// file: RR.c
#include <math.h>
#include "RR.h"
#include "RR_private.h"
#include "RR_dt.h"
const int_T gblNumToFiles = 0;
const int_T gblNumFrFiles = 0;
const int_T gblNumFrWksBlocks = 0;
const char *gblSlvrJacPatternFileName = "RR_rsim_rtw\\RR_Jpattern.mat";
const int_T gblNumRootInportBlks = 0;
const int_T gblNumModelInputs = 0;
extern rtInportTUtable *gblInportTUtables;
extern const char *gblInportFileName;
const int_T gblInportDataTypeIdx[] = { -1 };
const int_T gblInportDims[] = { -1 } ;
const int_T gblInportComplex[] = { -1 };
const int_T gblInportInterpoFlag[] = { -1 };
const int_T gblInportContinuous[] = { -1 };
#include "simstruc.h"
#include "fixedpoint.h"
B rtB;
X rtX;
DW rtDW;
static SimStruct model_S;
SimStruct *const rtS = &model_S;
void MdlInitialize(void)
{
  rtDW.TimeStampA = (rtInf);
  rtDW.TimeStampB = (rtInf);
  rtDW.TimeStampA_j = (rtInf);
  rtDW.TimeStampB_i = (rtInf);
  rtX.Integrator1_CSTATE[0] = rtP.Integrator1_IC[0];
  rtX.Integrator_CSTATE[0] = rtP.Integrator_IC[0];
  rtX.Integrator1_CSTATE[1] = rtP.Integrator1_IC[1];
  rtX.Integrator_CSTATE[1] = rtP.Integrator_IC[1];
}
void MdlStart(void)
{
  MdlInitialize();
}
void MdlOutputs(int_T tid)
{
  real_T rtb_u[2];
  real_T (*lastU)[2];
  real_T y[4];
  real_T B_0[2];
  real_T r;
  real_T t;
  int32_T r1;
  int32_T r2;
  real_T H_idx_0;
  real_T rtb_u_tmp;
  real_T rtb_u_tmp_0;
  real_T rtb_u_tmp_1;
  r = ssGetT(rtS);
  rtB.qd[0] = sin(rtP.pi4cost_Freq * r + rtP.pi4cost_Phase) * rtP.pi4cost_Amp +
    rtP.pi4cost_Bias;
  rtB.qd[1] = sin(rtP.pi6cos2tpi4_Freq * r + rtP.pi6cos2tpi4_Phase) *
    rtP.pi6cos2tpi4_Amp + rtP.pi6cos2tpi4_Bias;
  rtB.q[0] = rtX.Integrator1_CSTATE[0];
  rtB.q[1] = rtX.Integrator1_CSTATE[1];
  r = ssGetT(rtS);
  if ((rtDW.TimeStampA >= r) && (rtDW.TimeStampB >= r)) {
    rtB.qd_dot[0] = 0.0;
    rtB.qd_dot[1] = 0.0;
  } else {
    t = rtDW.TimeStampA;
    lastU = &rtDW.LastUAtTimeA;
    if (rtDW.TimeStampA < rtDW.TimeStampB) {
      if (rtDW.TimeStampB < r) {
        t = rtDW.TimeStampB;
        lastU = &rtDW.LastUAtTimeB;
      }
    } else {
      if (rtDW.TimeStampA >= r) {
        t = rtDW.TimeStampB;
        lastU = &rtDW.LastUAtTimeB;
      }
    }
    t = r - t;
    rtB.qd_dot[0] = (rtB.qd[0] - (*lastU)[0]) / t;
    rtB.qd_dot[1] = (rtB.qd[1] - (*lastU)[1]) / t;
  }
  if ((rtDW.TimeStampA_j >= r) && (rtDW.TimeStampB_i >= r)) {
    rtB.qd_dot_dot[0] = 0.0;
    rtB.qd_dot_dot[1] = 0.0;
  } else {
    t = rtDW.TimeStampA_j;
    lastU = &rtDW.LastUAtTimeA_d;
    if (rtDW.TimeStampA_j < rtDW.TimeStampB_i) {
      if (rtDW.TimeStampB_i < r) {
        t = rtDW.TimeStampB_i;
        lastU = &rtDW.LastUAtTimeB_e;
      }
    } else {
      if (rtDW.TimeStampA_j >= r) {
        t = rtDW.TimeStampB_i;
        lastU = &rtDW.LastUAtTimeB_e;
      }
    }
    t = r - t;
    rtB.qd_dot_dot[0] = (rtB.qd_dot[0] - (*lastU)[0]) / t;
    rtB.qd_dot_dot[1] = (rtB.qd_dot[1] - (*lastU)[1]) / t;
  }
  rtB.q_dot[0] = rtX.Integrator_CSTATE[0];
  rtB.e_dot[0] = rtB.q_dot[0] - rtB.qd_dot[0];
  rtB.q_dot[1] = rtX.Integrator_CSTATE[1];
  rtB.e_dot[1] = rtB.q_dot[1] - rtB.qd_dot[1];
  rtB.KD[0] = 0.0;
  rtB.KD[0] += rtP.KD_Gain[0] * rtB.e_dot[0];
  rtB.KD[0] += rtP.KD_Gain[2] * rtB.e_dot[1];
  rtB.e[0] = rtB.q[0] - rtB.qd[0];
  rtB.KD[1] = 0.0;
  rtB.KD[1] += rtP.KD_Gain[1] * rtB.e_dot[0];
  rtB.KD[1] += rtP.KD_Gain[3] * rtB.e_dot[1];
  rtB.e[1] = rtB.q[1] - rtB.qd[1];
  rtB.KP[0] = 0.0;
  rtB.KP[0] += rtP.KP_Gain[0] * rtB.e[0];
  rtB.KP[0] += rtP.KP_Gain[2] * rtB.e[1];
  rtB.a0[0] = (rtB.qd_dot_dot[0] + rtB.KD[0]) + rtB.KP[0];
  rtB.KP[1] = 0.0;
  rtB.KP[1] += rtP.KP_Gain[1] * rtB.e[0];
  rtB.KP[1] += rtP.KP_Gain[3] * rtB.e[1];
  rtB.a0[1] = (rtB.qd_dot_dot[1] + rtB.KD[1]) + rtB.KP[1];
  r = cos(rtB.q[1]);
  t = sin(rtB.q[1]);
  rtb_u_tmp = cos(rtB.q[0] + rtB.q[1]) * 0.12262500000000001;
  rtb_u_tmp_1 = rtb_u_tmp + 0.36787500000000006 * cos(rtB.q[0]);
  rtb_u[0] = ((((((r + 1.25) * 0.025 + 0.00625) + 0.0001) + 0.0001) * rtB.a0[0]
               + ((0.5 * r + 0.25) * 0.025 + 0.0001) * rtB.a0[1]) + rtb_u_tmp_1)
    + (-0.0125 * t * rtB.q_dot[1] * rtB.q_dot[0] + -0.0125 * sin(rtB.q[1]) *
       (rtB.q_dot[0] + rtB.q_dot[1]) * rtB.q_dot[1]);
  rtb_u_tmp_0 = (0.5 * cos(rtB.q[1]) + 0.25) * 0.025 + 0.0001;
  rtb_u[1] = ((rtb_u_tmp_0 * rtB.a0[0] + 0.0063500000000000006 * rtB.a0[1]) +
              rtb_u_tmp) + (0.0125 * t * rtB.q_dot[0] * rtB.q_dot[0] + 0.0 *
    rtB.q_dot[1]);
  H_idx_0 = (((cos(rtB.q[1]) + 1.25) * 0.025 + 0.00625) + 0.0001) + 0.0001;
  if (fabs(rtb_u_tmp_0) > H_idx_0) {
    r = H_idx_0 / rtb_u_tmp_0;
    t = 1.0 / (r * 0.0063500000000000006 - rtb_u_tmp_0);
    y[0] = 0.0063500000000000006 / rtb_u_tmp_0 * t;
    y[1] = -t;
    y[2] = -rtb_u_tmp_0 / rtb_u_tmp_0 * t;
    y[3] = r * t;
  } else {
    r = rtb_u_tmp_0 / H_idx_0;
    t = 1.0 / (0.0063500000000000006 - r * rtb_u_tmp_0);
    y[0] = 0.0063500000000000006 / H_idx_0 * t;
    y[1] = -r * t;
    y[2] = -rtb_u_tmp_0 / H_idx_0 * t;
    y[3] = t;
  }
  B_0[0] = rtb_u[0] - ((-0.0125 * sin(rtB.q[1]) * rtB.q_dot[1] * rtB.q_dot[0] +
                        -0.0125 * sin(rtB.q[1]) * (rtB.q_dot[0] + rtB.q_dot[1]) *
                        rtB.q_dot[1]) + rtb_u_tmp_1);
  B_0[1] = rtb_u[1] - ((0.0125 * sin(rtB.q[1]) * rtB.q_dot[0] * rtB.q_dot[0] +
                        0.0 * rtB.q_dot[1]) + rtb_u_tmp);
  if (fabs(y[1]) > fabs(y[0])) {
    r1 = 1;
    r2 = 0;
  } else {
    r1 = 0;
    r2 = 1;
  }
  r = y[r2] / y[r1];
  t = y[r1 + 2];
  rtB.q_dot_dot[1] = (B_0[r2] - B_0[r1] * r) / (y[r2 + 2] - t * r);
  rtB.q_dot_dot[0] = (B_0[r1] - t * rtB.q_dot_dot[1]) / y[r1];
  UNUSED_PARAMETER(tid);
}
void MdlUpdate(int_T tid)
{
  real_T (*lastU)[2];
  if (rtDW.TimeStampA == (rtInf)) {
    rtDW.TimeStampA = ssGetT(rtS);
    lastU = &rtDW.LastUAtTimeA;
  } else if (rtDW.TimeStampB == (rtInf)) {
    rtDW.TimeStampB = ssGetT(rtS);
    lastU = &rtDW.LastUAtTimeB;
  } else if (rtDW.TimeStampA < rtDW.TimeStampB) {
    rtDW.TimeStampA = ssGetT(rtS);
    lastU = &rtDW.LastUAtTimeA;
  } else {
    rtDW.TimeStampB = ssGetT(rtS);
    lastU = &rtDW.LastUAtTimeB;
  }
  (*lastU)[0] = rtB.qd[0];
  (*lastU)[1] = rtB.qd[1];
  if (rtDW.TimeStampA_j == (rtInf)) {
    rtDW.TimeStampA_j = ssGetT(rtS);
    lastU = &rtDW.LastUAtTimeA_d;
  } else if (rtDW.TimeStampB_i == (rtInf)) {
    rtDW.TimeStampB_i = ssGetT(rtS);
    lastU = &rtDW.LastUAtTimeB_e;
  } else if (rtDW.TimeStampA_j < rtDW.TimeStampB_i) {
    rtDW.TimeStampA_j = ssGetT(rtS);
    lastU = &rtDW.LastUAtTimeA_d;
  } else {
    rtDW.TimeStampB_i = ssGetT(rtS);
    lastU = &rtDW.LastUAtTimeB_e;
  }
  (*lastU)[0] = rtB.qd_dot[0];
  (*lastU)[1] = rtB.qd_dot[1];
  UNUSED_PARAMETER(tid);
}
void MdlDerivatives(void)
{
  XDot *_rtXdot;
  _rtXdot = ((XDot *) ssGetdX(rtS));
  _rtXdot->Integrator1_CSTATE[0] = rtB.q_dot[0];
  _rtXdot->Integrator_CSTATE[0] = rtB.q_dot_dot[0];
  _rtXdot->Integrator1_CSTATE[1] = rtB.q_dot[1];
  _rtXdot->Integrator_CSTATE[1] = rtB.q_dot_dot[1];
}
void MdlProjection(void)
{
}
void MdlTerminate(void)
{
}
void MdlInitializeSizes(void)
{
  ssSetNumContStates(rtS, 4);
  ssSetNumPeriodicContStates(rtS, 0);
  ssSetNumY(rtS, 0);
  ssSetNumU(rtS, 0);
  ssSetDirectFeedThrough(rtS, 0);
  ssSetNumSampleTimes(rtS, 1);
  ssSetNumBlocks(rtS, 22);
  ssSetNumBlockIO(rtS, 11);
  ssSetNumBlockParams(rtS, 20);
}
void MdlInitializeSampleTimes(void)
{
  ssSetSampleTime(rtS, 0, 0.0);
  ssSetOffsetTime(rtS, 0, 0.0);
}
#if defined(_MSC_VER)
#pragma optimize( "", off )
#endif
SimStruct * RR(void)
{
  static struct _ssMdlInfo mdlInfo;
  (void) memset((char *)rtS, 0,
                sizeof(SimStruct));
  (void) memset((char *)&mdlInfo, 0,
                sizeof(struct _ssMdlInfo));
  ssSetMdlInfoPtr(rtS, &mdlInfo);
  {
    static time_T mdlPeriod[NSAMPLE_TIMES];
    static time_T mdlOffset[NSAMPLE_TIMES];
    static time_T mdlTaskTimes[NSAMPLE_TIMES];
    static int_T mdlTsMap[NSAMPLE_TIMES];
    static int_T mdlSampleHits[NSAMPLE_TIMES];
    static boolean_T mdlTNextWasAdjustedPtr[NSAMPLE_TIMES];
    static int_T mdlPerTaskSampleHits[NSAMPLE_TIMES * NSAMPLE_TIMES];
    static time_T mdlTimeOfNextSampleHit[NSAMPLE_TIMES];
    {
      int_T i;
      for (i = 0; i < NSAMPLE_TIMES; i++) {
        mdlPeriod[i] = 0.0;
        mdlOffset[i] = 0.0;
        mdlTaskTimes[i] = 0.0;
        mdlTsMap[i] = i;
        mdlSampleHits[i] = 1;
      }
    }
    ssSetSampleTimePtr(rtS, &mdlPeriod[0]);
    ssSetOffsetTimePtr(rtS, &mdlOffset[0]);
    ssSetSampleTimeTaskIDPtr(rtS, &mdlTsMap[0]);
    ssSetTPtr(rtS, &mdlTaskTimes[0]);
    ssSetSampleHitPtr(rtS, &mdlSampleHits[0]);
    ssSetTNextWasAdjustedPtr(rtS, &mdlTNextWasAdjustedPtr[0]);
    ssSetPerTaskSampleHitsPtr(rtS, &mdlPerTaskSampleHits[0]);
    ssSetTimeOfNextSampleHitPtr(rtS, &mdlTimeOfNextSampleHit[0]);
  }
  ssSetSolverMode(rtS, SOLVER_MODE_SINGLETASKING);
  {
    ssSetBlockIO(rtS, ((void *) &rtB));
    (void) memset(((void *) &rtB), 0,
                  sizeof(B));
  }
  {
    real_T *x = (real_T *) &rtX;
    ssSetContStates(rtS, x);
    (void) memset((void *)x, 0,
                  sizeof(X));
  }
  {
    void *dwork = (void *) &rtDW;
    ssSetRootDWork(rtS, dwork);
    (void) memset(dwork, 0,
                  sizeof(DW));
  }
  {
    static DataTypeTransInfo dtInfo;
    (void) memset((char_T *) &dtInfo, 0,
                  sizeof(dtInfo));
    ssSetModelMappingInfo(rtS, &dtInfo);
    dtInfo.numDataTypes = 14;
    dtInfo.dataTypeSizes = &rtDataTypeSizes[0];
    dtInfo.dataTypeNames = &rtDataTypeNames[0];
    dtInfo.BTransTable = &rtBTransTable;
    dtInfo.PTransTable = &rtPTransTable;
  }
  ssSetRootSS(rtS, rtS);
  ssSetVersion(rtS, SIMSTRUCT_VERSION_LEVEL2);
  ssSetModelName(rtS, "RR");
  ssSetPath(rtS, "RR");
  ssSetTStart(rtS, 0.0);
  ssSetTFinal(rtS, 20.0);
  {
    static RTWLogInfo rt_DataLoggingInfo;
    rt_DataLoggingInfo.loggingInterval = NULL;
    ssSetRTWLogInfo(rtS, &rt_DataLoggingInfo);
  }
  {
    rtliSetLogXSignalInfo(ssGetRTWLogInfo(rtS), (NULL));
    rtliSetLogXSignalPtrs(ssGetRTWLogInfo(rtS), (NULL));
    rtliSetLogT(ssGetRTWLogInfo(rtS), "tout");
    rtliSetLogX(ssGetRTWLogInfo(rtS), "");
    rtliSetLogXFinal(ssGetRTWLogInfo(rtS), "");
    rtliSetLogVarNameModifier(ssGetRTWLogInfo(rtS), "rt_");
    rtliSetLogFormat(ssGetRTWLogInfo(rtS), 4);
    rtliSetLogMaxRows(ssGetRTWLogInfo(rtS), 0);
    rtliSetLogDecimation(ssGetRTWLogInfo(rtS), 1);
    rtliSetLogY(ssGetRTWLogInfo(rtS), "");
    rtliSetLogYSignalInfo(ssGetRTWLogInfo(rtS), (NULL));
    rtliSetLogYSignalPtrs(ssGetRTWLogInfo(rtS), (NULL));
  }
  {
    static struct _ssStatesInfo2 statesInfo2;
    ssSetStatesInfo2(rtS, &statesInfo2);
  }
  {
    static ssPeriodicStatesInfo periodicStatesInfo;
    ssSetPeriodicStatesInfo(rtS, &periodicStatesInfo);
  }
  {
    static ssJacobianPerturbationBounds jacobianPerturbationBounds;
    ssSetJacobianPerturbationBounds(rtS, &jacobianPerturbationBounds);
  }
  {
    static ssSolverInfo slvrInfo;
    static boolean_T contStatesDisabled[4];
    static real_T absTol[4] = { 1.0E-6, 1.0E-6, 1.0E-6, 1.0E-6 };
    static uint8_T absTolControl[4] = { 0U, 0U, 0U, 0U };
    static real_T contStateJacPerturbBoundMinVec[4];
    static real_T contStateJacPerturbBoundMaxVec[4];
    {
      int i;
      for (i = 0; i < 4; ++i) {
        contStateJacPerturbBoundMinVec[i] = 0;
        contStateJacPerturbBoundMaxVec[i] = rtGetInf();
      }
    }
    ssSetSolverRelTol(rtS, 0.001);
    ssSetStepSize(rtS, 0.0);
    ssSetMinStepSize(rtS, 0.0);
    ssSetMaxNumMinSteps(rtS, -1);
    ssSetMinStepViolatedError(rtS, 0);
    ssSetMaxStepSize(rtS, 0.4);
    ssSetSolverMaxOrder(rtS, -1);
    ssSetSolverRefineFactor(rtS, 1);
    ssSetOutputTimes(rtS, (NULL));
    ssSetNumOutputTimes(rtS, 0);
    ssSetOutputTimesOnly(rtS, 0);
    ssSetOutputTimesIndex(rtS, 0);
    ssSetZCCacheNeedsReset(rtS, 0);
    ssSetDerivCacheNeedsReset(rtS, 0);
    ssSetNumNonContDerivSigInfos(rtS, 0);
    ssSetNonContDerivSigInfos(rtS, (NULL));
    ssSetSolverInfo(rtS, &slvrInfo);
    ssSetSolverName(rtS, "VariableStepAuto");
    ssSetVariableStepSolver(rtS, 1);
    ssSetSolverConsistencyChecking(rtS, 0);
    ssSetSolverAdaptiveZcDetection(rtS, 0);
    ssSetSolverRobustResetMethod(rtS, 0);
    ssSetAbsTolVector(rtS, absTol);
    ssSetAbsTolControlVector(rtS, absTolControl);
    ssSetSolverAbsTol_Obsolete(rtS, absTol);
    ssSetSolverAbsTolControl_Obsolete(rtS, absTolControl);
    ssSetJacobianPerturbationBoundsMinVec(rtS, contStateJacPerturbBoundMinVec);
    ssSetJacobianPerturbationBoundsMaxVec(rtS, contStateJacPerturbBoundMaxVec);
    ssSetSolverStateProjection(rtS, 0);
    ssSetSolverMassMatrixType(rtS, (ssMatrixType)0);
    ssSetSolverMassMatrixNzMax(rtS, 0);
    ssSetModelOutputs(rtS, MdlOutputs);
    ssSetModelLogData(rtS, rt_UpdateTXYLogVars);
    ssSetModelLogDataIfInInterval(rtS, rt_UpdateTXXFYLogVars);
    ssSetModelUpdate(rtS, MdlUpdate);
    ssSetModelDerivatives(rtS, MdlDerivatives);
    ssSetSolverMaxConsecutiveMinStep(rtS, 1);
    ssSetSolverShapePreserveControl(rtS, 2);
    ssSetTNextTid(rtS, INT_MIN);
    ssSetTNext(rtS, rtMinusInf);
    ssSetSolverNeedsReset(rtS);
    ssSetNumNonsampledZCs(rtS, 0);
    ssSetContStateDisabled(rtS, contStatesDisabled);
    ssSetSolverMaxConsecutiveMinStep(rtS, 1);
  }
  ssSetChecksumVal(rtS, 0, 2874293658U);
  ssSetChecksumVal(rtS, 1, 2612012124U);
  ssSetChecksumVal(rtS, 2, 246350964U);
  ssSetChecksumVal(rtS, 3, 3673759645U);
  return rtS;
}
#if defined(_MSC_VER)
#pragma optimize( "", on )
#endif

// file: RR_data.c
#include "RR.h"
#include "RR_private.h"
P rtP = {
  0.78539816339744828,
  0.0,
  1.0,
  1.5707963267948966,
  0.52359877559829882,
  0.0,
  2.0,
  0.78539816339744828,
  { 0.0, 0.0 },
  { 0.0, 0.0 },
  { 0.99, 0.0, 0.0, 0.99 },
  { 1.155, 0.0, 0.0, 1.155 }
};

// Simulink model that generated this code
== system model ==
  Derivative#1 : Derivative  <- 1: qd
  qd : MATLAB Function  <- 1: pi4cost, 2: pi6cos2tpi4
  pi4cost : Sin  Amplitude=pi/4  Phase=pi/2
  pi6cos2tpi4 : Sin  Amplitude=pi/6  Frequency=2  Phase=pi/4
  Derivative#2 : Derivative  <- 1: Derivative#1
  Integrator1 : Integrator  InitialCondition=[0;0]  <- 1: Integrator
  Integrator : Integrator  InitialCondition=[0;0]  <- 1: MATLABFunction#1
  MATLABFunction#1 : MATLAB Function  <- 1: MATLABFunction#2, 2: Integrator1, 3: Integrator
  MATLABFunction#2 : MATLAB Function  <- 1: Sum#1, 2: Integrator1, 3: Integrator
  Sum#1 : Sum  Inputs=+++  <- 1: Derivative#2, 2: KD, 3: KP
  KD : Gain  Gain=[0.99 0;0 0.99]  Multiplication=Matrix(K*u) (u vector)  <- 1: Sum#2
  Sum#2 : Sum  Inputs=-+  <- 1: Derivative#1, 2: Integrator
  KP : Gain  Gain=[1.155 0;0 1.155]  Multiplication=Matrix(K*u) (u vector)  <- 1: Sum#3
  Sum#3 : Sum  Inputs=-+  <- 1: qd, 2: Integrator1
== matlab function MATLABFunction#2 ==
function u  = Control(a0,q,q_dot)
q1=q(1,1);
q2=q(2,1);
q1_dot=q_dot(1,1);
q2_dot=q_dot(2,1);
m1=0.025;
m2=0.025;
l1=1;
lc1=0.5;
lc2=0.5;
q2=q(2,1);
q1_dot=q_dot(1,1);
q2_dot=q_dot(2,1);
I1=0.0001;
I2=0.0001;
g=9.81;

c11=-m2*l1*lc2*sin(q2)*q2_dot;
c12=-m2*l1*lc2*sin(q2)*(q1_dot+q2_dot);
c21=m2*l1*lc2*(sin(q2))*q1_dot;
c22=0;

C = [c11 c12; c21 c22];

g1= (m1*lc1+m2*l1)*g*cos(q1) + m2*lc2*g*cos(q1+q2);
g2= m2*lc2*g*cos(q1+q2);

G=[g1;g2];

h11= m1*lc1^2 + m2*(l1^2+lc2^2+2*l1*lc2*(cos(q2)))+I1+I2;
h12= m2*(lc2^2 + l1*lc2*(cos(q2)))+ I2;
h21= m2*(lc2^2 + l1*lc2*(cos(q2)))+ I2;
h22= m2*lc2^2 + I2;
H=[h11 h12; h21 h22];
    
u=H*a0+G+C*q_dot;
  
end

== matlab function MATLABFunction#1 ==
function q_dot_dot  = Manipulator(u,q,q_dot)
q1=q(1,1);
q2=q(2,1);
q1_dot=q_dot(1,1);
q2_dot=q_dot(2,1);
m1=0.025;
m2=0.025;
l1=1;
lc1=0.5;
lc2=0.5;
u1 = u(1,1);
u2 = u(2,1);
q2=q(2,1);
q1_dot=q_dot(1,1);
q2_dot=q_dot(2,1);
I1=0.0001;
I2=0.0001;
g=9.81;

c11=-m2*l1*lc2*sin(q2)*q2_dot;
c12=-m2*l1*lc2*sin(q2)*(q1_dot+q2_dot);
c21=m2*l1*lc2*(sin(q2))*q1_dot;
c22=0;

C = [c11 c12; c21 c22];

g1= (m1*lc1+m2*l1)*g*cos(q1) + m2*lc2*g*cos(q1+q2);
g2= m2*lc2*g*cos(q1+q2);

G=[g1;g2];

h11= m1*lc1^2 + m2*(l1^2+lc2^2+2*l1*lc2*(cos(q2)))+I1+I2;
h12= m2*(lc2^2 + l1*lc2*(cos(q2)))+ I2;
h21= m2*(lc2^2 + l1*lc2*(cos(q2)))+ I2;
h22= m2*lc2^2 + I2;
H=[h11 h12; h21 h22];
    
    tou = [u1 u2]';
    tou_1 = C*[q1_dot q2_dot]'+ G;
    
    q_dot_dot = inv(H)\(tou-tou_1);
    
  
end

== matlab function qd ==
function qd  = qd_calculator(q1d,q2d)

qd=[q1d; q2d];

end
